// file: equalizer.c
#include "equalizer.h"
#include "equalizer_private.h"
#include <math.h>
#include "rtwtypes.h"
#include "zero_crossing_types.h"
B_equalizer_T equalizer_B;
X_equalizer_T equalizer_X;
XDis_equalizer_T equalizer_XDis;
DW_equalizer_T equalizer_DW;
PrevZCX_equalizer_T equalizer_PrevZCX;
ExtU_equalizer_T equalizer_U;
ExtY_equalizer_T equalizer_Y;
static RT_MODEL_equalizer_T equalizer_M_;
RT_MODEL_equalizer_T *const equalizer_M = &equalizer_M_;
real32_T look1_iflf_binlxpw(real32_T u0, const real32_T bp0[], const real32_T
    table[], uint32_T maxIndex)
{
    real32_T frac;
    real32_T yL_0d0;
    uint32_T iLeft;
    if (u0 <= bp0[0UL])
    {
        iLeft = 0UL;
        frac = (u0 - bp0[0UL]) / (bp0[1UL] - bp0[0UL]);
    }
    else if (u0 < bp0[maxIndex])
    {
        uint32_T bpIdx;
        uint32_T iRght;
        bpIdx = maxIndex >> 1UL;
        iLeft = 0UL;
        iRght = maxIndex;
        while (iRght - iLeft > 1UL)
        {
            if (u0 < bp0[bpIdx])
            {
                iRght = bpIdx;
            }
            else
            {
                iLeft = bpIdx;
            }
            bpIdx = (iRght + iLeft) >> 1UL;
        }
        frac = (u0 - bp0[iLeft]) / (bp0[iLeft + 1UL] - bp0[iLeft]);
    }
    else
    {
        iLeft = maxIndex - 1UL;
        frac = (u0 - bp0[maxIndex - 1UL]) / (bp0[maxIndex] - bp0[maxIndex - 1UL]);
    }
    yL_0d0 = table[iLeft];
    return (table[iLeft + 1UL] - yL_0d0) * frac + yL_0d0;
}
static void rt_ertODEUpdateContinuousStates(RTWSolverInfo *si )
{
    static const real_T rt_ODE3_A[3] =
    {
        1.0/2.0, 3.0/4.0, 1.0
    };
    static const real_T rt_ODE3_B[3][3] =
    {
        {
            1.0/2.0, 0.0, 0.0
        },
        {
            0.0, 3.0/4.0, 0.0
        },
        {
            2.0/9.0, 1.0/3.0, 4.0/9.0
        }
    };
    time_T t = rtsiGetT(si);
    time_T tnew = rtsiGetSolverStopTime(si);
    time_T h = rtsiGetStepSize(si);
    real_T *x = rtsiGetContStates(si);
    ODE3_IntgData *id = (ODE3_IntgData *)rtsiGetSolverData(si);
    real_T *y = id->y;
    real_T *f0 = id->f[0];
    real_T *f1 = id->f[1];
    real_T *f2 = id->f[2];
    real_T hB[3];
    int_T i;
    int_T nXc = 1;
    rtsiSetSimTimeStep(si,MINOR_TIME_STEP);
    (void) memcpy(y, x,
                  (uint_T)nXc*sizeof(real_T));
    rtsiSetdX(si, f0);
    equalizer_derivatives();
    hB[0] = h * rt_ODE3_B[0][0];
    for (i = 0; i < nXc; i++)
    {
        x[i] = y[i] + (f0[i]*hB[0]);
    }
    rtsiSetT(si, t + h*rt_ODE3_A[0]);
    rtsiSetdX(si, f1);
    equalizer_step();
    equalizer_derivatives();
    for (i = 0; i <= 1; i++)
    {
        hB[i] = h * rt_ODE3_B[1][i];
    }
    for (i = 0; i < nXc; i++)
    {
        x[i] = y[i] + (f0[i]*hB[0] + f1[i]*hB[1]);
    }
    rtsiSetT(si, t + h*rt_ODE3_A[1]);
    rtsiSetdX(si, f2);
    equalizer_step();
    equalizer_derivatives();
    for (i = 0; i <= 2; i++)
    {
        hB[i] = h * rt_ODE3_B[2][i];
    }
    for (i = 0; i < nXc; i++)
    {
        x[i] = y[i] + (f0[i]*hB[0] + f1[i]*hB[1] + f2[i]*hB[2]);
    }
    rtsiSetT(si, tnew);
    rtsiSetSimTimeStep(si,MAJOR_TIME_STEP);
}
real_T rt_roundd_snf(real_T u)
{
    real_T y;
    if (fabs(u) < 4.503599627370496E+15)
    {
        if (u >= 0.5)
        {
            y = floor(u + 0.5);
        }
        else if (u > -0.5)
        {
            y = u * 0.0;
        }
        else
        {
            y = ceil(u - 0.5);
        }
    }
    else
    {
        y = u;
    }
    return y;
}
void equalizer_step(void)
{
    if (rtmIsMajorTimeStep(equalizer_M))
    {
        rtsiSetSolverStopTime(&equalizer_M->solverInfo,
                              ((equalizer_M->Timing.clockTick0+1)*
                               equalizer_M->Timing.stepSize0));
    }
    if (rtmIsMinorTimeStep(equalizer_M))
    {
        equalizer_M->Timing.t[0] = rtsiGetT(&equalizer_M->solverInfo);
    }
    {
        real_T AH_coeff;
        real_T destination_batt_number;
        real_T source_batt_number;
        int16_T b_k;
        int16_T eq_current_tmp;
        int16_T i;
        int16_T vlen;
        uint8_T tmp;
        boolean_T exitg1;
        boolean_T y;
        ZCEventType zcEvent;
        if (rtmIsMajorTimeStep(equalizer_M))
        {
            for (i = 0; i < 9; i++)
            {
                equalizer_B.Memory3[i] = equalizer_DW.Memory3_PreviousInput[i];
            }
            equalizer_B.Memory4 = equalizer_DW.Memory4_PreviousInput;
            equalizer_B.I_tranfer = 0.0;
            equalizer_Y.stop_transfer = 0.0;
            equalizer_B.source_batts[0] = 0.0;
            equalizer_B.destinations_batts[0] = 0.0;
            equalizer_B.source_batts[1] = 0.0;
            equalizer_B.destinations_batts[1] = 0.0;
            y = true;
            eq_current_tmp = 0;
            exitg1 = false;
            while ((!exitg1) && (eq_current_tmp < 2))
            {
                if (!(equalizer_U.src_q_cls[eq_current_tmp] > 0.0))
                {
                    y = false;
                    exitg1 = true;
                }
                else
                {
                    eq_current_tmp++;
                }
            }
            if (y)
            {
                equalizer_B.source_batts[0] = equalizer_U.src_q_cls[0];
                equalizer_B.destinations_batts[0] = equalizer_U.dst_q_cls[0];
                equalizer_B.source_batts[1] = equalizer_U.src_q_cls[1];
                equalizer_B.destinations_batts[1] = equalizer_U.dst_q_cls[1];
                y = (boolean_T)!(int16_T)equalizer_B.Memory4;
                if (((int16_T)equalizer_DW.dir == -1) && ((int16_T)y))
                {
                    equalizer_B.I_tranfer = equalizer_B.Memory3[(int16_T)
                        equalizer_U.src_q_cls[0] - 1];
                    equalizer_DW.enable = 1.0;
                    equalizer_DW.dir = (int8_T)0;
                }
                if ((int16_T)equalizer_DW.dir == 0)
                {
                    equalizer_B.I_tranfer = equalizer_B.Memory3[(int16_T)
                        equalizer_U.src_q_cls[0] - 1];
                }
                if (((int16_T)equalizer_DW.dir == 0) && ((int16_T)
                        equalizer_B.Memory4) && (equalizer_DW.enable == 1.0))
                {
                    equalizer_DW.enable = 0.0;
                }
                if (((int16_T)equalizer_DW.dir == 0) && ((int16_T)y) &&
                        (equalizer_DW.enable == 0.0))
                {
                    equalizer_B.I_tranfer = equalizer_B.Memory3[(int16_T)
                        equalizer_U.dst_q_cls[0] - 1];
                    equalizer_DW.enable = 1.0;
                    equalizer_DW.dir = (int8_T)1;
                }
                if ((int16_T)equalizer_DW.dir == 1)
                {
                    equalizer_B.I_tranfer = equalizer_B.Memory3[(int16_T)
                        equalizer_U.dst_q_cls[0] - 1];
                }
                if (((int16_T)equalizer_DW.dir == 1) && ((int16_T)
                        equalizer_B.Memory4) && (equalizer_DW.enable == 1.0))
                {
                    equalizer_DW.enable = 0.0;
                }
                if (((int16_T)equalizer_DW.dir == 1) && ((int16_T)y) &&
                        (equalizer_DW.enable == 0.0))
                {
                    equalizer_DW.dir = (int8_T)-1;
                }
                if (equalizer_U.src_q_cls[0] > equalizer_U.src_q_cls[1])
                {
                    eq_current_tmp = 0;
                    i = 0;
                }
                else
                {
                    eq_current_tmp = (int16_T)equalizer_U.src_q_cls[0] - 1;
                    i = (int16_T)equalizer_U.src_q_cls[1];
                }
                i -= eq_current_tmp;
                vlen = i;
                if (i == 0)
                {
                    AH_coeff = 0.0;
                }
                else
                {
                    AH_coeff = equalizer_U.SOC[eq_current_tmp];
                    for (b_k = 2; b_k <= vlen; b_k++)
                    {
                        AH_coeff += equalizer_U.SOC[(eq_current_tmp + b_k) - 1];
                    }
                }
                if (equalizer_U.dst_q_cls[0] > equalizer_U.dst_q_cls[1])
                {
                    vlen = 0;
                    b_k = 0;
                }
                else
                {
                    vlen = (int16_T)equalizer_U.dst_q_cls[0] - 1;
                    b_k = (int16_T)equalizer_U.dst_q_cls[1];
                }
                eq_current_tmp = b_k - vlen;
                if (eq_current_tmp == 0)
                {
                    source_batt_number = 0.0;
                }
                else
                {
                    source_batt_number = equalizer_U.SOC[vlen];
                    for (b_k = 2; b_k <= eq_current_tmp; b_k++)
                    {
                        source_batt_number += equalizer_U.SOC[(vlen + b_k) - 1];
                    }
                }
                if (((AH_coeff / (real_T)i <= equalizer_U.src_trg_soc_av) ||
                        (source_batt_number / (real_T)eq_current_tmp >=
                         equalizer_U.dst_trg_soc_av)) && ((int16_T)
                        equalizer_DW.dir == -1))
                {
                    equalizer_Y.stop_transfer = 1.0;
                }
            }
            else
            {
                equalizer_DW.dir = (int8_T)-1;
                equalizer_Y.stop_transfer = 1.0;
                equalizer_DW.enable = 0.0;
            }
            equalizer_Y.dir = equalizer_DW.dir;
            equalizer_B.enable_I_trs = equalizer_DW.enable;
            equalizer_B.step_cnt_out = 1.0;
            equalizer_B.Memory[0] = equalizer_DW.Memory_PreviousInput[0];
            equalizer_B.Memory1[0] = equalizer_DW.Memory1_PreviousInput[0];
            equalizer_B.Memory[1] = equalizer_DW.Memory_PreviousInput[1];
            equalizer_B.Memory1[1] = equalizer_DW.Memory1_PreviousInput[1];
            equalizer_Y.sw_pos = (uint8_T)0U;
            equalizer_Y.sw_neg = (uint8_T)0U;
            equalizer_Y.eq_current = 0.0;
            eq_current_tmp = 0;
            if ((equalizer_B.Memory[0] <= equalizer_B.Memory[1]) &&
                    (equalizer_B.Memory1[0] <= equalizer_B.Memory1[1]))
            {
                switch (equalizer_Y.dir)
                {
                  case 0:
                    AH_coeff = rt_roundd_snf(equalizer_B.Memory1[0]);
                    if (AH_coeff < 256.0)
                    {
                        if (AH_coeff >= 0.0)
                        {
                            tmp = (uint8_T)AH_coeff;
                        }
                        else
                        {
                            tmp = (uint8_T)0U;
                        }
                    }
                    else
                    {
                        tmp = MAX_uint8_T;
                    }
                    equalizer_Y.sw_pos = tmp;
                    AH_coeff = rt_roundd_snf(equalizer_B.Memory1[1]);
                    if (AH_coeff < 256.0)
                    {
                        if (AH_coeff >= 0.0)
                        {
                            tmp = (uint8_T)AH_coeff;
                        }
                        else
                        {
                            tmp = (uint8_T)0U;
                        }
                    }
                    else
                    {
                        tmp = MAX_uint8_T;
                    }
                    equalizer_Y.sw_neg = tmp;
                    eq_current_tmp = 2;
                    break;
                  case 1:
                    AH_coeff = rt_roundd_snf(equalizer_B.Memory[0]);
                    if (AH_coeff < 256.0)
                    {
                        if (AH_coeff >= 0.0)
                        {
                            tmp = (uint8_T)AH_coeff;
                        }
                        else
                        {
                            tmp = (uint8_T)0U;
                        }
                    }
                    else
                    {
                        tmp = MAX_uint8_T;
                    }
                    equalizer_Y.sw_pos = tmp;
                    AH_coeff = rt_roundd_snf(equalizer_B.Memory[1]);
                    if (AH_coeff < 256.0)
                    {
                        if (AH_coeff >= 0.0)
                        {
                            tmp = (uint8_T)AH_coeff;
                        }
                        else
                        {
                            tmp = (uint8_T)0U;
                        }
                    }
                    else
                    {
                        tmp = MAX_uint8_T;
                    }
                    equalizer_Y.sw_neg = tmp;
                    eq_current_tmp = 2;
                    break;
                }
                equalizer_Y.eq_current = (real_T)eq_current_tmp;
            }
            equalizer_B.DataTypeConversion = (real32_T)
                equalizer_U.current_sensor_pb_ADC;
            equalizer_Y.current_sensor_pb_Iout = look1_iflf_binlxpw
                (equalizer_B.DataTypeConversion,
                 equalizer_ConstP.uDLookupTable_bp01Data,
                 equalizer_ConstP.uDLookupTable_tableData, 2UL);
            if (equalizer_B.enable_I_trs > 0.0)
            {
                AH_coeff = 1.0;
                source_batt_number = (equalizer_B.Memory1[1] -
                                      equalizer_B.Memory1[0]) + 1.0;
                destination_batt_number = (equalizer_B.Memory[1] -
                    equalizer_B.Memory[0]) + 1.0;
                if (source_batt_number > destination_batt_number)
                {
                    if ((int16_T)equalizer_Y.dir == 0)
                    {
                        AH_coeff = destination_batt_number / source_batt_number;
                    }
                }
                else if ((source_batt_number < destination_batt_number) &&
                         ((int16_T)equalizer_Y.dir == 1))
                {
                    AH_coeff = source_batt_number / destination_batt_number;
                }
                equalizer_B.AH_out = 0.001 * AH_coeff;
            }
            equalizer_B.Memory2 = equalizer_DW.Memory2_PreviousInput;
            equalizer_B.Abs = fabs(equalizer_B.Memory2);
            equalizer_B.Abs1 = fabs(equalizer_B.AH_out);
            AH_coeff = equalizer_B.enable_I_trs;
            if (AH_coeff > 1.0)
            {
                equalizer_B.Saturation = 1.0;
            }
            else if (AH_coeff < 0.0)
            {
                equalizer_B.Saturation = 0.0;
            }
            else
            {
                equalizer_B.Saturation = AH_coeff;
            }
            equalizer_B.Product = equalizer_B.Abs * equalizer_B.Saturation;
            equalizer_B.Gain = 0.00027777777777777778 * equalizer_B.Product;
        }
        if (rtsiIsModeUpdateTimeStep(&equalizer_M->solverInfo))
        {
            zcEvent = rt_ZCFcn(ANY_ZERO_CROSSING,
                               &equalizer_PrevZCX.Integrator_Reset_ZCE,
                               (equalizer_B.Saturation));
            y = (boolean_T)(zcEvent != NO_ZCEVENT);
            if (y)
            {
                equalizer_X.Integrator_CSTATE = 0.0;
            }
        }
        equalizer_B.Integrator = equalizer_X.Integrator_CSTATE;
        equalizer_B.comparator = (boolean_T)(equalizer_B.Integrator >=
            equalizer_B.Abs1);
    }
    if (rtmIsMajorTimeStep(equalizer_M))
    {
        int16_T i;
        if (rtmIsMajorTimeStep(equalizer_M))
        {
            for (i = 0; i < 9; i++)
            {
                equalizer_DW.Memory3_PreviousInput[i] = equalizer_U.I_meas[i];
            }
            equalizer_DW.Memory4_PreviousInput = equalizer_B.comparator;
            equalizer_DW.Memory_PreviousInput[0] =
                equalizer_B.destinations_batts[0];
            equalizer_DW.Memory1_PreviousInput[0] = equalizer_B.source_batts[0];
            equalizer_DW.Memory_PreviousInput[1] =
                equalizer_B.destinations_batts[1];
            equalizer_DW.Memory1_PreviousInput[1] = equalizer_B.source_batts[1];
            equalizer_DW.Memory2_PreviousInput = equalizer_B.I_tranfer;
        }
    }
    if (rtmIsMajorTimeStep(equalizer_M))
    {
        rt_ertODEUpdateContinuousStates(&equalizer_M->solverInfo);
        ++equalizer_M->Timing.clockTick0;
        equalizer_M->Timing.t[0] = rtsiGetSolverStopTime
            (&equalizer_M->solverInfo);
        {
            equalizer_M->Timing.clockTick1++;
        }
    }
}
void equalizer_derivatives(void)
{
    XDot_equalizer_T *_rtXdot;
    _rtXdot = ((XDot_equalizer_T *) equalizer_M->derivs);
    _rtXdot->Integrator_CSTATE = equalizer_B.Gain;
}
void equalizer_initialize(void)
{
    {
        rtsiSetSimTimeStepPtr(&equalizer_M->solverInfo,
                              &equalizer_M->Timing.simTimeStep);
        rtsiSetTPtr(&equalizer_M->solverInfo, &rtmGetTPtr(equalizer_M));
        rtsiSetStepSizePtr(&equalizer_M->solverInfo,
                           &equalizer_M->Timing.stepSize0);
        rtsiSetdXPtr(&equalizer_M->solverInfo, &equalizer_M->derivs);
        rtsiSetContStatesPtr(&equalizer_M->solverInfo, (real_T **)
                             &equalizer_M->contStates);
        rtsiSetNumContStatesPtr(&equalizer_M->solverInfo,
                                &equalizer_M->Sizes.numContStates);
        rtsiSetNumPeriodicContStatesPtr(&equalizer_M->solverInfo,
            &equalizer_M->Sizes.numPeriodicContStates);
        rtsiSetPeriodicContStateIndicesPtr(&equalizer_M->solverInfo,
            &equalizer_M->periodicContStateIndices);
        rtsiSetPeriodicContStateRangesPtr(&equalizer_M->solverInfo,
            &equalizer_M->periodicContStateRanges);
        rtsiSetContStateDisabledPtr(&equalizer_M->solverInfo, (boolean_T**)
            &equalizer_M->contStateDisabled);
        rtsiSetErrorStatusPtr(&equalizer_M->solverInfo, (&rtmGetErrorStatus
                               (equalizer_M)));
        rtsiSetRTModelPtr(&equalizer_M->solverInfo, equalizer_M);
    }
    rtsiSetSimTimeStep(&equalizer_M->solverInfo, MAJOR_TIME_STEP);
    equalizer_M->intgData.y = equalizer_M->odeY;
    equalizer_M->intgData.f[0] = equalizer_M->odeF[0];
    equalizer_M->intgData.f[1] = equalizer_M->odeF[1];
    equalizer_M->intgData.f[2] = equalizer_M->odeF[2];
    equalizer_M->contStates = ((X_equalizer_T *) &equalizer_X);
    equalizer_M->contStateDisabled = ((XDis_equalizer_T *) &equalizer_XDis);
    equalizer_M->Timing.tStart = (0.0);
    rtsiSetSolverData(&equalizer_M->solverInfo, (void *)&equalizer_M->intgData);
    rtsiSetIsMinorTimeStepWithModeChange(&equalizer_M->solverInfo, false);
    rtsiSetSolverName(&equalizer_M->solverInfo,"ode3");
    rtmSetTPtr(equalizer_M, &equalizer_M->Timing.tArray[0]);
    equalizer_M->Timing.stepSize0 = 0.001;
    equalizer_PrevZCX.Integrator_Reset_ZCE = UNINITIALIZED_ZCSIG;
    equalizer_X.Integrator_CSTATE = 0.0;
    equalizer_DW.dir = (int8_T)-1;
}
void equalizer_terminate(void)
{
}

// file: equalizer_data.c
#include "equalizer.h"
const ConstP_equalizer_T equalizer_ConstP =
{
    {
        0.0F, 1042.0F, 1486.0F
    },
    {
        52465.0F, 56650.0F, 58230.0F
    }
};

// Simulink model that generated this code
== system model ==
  src_q_cls : Inport
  dst_q_cls : Inport
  src_trg_soc_av : Inport
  dst_trg_soc_av : Inport
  SOC : Inport
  Inport#1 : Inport
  I_meas : Inport
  Inport#2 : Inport
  current_sensor_pb_ADC : Inport
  dir : Outport  <- 1: equalizer/5
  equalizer : MATLAB Function  <- 1: SOC, 2: src_q_cls, 3: dst_q_cls, 4: src_trg_soc_av, 5: dst_trg_soc_av, 6: Memory3, 7: Memory4
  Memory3 : Memory  <- 1: I_meas
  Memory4 : Memory  <- 1: comparator
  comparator : RelationalOperator  <- 1: Integrator, 2: Abs1
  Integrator : Integrator  ExternalReset=either  <- 1: Gain, 2: Saturation
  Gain : Gain  Gain=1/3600  <- 1: Product
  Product : Product  <- 1: Abs, 2: Saturation
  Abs : Abs  <- 1: Memory2
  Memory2 : Memory  <- 1: equalizer/6
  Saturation : Saturate  UpperLimit=1  LowerLimit=0  <- 1: equalizer/7
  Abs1 : Abs  <- 1: Subsystem#1
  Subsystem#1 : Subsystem  <- 1: Memory, 2: Memory1, 3: equalizer/5, Enable: equalizer/7
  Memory : Memory  <- 1: equalizer
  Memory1 : Memory  <- 1: equalizer/2
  eq_current : Outport  <- 1: MATLABFunction#1/3
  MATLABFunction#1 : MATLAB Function  <- 1: Memory, 2: Memory1, 3: equalizer/5
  Outport#1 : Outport
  stop_transfer : Outport  <- 1: equalizer/4
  sw_pos : Outport  <- 1: MATLABFunction#1
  sw_neg : Outport  <- 1: MATLABFunction#1/2
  current_sensor_pb_Iout : Outport  <- 1: Lookup_nD#1
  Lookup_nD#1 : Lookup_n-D  BreakpointsForDimension1=[52465 56650 58230]  Table=[0 1042 1486]  <- 1: DataTypeConversion
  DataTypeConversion : DataTypeConversion  <- 1: current_sensor_pb_ADC
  Gain#1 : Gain  Gain=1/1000  <- 1: Inport#2
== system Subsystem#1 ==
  destination_batt : Inport
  source_batt : Inport
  Inport#3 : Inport
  EnablePort#1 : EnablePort
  AH_out : Outport  <- 1: MATLABFunction#2
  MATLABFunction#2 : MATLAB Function  <- 1: destination_batt, 2: source_batt, 3: Inport#3
== matlab function MATLABFunction#1 ==
function [sw_pos, sw_neg, eq_current] = battery_selector(batts_to_charge, batts_to_discharge, direction)
    sw_pos = uint8(0);
    sw_neg = uint8(0);
    eq_current = 0;
    eq_current_tmp = 0;
% to prevent invalid switch selection
if ( batts_to_charge(1, 1) <= batts_to_charge(1, 2) && ...
     batts_to_discharge(1, 1) <= batts_to_discharge(1, 2))
    
    % charge the capacitor using batteries
    if(direction == 0)
        sw_pos = uint8(batts_to_discharge(1, 1));
        sw_neg = uint8(batts_to_discharge(1, 2));
        eq_current_tmp = 2;        
    % charge the battery using capacitor
    elseif(direction == 1)
        sw_pos = uint8(batts_to_charge(1, 1));
        sw_neg = uint8(batts_to_charge(1, 2));
        eq_current_tmp = 2;
    else
        sw_pos = uint8(0);
        sw_neg = uint8(0);
    end

    eq_current = eq_current_tmp;

end

end

== matlab function equalizer ==
function [destinations_batts, source_batts, step_cnt_out, stop_transfer, direction, I_tranfer, enable_I_trs] = ...
    battery_selector ...
    (SOC, src_q_cls, dst_q_cls, src_trg_soc_av, dst_trg_soc_av, I_meas, flg_chrg_trs)

I_tranfer  = 0;
stop_transfer  = 0;
source_batts = [0 0];
destinations_batts = [0 0];
dst_trg_soc_av_tmp = dst_trg_soc_av;
src_trg_soc_av_tmp = src_trg_soc_av;

%dst_trg_soc_av_tmp(dst_trg_soc_av == 0) = Inf;
% src_trg_soc_av_tmp(src_trg_soc_av == 0) = Inf;
% the number of steps to equlalize the battery pack
step = length(src_q_cls);

persistent step_cnt;
persistent I_cells_source;
persistent I_cells_destination;
persistent dir;
persistent enable;

if isempty(step_cnt)
    step_cnt = 1;
    assert(1, 'Simulation terminated because x >= 10')

end

if isempty(I_cells_source)
    I_cells_source = 0;
end
if isempty(I_cells_destination)
    I_cells_destination = 0;
end
if isempty(dir)
    dir = int8(-1);
end
if isempty(enable)
    enable = 0;
end

soc = SOC';
if src_q_cls(1, :) > 0

    source_batts = src_q_cls(1, :);
    I_cells_source = I_meas(source_batts(1, 1));       % source cells current
    destinations_batts = dst_q_cls(1, :);
    I_cells_destination = I_meas(destinations_batts(1, 1));  % destication cells current

    if(dir == -1 && flg_chrg_trs == 0) % dischaege source if in the begining of charge transfering
        I_tranfer = I_cells_source;
        enable = 1; % start counting coulombs
        dir = int8(0); 
    end
    if(dir == 0)
        I_tranfer = I_cells_source;
    end

    if(dir == 0 && flg_chrg_trs == 1 && enable == 1) % reset the flag
        enable = 0;
    end

    if(dir == 0 && flg_chrg_trs == 0 && enable == 0) % charge the destination if the prevoius charge transfer terminated
        I_tranfer = I_cells_destination;
        enable = 1;
        dir = int8(1);
    end
    if(dir == 1)
        I_tranfer = I_cells_destination;
    end

    if(dir == 1 && flg_chrg_trs == 1 && enable == 1) % reset the flag
        enable = 0;
    end

    if(dir == 1 && flg_chrg_trs == 0 && enable == 0) % charge transfer terminated
        dir = int8(-1);
    end
    
    sm = mean(soc(src_q_cls(1, 1):src_q_cls(1, 2)));
    dm = mean(soc(dst_q_cls(1, 1):dst_q_cls(1, 2)));
    if(sm <= src_trg_soc_av_tmp(1) || dm >= dst_trg_soc_av_tmp(1)) && dir == -1
        stop_transfer = 1;
    end
else
    direction = int8(0);
    I_cells_source = 0;
    I_cells_destination = 0;
    dir = int8(-1);
    stop_transfer  = 1;
    enable = 0;
end
direction = int8(dir);
enable_I_trs = enable;

step_cnt_out = step_cnt;

end

== matlab function MATLABFunction#2 ==
function AH_out = fcn(destination_batt, source_batt, direction)
AH_base = 0.001;
AH_coeff = 1;
AH_out = 0;

source_batt_number = source_batt(1, 2) - source_batt(1, 1) + 1;
destination_batt_number = destination_batt(1, 2) - destination_batt(1, 1) + 1;

if (source_batt_number > destination_batt_number)
    if direction == 0
        AH_coeff = destination_batt_number / source_batt_number;
    else
        AH_coeff = 1; 
    end
elseif source_batt_number < destination_batt_number
     if direction == 1
        AH_coeff = source_batt_number / destination_batt_number;
    else
        AH_coeff = 1; 
    end
end

AH_out = AH_base * AH_coeff;
